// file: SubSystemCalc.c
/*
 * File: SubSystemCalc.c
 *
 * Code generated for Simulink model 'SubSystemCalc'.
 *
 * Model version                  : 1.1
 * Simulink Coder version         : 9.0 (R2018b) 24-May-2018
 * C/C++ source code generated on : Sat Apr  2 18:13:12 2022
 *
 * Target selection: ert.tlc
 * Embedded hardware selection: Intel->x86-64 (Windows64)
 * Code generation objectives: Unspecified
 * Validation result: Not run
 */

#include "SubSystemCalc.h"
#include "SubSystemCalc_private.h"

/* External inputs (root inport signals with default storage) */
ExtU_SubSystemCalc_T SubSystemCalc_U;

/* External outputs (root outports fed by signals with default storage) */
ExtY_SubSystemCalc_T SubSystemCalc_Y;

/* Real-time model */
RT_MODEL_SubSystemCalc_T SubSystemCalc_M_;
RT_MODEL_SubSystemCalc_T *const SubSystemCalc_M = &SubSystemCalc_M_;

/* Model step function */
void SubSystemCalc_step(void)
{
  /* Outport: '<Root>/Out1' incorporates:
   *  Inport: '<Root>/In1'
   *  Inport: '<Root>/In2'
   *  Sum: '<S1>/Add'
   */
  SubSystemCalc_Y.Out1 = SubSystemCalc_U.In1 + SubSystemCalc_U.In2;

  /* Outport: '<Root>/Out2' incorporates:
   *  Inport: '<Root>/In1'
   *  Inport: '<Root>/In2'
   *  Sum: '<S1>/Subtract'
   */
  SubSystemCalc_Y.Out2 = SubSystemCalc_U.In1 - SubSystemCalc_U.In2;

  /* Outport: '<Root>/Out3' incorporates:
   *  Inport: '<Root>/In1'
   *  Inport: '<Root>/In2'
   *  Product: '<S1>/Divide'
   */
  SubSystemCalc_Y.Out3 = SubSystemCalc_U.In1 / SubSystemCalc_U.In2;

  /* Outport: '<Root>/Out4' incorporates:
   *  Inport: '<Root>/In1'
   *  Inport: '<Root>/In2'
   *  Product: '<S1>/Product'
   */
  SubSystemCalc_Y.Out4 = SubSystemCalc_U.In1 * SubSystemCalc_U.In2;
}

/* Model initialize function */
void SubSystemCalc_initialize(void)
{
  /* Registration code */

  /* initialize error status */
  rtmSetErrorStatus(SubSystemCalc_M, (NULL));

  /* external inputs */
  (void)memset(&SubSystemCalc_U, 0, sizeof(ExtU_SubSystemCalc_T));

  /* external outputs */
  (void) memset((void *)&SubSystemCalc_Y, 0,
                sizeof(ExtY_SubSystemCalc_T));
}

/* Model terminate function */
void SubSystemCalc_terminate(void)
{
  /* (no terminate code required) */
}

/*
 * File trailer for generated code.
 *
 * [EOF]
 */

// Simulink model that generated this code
simulink model "SubSystemCalc"  (R2018b)
settings: Solver=FixedStepDiscrete  StartTime=0.0  StopTime=10.0  RelTol=1e-3

== system SubSystemCalc ==
  In1 : Inport
  In2 : Inport  Port=2
  Subsystem : Subsystem
  Out1 : Outport
  Out2 : Outport  Port=2
  Out3 : Outport  Port=3
  Out4 : Outport  Port=4
  wires:
  In1/1 -> Subsystem/1(In1)
  In2/1 -> Subsystem/2(In2)
  Subsystem/1(Out1) -> Out1/1
  Subsystem/2(Out2) -> Out2/1
  Subsystem/3(Out3) -> Out3/1
  Subsystem/4(Out4) -> Out4/1

== system SubSystemCalc/Subsystem ==
  In1 : Inport
  In2 : Inport  Port=2
  Add : Sum
  Divide : Product  Inputs=*/
  Product : Product
  Subtract : Sum  Inputs=+-
  Out1 : Outport
  Out2 : Outport  Port=2
  Out3 : Outport  Port=3
  Out4 : Outport  Port=4
  wires:
  Add/1 -> Out1/1
  In1/1 -> Divide/1, Subtract/1, Product/1, Add/1
  Divide/1 -> Out3/1
  In2/1 -> Divide/2, Subtract/2, Product/2, Add/2
  Subtract/1 -> Out2/1
  Product/1 -> Out4/1
